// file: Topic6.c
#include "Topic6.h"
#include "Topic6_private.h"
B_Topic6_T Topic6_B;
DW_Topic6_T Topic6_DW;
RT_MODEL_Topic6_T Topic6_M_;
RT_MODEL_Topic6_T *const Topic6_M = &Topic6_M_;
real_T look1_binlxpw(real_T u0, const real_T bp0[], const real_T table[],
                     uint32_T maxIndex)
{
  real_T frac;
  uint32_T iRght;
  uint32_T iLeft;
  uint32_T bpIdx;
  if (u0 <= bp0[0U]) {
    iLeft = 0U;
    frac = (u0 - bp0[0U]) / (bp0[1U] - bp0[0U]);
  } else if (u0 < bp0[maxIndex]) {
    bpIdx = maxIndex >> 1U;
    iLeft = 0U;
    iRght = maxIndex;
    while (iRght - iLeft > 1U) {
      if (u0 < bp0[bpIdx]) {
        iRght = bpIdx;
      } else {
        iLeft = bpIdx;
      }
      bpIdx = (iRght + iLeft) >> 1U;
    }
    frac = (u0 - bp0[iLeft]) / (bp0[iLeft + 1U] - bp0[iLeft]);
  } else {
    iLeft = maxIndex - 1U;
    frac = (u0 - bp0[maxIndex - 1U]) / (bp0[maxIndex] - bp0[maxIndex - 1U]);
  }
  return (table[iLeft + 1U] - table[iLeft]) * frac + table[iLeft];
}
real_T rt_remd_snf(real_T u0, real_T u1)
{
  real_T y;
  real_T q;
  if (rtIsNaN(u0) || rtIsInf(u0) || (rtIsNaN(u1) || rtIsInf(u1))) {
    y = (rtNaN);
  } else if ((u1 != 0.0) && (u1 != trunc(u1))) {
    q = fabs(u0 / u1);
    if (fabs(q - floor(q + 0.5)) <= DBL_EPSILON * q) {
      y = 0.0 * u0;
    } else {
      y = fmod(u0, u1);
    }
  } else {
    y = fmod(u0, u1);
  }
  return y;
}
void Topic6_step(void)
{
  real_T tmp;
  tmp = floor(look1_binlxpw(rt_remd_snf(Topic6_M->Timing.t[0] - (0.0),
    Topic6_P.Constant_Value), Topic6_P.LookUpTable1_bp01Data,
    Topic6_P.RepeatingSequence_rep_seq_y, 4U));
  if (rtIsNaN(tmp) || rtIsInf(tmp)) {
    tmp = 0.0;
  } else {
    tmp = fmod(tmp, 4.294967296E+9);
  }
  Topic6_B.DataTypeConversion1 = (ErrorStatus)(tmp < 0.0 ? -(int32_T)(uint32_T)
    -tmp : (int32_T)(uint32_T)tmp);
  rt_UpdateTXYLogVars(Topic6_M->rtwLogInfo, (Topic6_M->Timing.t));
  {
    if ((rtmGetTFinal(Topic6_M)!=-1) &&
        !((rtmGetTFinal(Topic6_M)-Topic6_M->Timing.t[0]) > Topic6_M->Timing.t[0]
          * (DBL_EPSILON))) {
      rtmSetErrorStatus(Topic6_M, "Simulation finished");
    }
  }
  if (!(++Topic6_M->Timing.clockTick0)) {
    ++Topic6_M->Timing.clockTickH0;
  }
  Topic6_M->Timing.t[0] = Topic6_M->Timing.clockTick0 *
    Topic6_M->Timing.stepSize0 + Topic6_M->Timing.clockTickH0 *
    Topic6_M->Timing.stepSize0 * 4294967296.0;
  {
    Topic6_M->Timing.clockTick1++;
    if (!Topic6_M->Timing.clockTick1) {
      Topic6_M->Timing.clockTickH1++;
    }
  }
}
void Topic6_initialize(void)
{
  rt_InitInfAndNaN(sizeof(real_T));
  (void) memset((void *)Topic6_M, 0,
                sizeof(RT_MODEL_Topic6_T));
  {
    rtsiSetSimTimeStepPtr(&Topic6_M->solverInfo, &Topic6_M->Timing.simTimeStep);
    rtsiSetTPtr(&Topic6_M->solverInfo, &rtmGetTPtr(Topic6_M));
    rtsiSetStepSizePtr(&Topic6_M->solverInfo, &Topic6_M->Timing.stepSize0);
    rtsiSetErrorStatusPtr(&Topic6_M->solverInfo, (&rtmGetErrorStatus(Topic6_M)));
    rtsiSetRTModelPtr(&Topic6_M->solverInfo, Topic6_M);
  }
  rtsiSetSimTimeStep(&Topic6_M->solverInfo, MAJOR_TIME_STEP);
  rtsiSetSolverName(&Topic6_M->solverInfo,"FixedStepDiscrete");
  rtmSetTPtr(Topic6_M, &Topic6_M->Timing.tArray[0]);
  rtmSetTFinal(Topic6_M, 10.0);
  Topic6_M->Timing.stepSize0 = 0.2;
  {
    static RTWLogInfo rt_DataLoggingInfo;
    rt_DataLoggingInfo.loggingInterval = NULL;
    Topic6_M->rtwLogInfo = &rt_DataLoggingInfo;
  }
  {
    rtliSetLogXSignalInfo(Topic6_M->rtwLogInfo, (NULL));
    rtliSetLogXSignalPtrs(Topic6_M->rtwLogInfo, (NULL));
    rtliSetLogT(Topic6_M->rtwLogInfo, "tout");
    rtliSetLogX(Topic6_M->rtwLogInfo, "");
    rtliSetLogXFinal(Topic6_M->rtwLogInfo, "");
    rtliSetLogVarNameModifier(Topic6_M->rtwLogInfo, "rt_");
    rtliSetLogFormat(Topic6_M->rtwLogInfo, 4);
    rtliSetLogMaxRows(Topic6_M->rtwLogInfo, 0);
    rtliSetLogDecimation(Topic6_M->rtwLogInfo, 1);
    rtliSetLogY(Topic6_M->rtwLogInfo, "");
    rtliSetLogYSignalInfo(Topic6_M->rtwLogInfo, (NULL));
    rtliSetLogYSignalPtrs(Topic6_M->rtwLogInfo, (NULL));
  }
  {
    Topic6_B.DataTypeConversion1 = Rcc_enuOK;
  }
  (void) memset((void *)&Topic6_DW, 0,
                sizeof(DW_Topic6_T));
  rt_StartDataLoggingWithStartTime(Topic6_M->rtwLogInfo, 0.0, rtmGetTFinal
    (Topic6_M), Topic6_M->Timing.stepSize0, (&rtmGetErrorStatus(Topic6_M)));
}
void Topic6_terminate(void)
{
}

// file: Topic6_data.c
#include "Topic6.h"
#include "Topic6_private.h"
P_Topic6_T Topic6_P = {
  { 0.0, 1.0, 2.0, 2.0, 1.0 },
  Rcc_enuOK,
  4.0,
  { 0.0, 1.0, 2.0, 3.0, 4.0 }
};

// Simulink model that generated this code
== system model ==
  DataTypeConversion1 : DataTypeConversion  <- 1: DataTypeConversion#1
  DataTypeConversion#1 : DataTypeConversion  <- 1: RepeatingSequence
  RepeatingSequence : simulink/Sources/Repeating Sequence
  EnumeratedConstant#1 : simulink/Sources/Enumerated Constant  Value=ErrorStatus.Rcc_enuOK
